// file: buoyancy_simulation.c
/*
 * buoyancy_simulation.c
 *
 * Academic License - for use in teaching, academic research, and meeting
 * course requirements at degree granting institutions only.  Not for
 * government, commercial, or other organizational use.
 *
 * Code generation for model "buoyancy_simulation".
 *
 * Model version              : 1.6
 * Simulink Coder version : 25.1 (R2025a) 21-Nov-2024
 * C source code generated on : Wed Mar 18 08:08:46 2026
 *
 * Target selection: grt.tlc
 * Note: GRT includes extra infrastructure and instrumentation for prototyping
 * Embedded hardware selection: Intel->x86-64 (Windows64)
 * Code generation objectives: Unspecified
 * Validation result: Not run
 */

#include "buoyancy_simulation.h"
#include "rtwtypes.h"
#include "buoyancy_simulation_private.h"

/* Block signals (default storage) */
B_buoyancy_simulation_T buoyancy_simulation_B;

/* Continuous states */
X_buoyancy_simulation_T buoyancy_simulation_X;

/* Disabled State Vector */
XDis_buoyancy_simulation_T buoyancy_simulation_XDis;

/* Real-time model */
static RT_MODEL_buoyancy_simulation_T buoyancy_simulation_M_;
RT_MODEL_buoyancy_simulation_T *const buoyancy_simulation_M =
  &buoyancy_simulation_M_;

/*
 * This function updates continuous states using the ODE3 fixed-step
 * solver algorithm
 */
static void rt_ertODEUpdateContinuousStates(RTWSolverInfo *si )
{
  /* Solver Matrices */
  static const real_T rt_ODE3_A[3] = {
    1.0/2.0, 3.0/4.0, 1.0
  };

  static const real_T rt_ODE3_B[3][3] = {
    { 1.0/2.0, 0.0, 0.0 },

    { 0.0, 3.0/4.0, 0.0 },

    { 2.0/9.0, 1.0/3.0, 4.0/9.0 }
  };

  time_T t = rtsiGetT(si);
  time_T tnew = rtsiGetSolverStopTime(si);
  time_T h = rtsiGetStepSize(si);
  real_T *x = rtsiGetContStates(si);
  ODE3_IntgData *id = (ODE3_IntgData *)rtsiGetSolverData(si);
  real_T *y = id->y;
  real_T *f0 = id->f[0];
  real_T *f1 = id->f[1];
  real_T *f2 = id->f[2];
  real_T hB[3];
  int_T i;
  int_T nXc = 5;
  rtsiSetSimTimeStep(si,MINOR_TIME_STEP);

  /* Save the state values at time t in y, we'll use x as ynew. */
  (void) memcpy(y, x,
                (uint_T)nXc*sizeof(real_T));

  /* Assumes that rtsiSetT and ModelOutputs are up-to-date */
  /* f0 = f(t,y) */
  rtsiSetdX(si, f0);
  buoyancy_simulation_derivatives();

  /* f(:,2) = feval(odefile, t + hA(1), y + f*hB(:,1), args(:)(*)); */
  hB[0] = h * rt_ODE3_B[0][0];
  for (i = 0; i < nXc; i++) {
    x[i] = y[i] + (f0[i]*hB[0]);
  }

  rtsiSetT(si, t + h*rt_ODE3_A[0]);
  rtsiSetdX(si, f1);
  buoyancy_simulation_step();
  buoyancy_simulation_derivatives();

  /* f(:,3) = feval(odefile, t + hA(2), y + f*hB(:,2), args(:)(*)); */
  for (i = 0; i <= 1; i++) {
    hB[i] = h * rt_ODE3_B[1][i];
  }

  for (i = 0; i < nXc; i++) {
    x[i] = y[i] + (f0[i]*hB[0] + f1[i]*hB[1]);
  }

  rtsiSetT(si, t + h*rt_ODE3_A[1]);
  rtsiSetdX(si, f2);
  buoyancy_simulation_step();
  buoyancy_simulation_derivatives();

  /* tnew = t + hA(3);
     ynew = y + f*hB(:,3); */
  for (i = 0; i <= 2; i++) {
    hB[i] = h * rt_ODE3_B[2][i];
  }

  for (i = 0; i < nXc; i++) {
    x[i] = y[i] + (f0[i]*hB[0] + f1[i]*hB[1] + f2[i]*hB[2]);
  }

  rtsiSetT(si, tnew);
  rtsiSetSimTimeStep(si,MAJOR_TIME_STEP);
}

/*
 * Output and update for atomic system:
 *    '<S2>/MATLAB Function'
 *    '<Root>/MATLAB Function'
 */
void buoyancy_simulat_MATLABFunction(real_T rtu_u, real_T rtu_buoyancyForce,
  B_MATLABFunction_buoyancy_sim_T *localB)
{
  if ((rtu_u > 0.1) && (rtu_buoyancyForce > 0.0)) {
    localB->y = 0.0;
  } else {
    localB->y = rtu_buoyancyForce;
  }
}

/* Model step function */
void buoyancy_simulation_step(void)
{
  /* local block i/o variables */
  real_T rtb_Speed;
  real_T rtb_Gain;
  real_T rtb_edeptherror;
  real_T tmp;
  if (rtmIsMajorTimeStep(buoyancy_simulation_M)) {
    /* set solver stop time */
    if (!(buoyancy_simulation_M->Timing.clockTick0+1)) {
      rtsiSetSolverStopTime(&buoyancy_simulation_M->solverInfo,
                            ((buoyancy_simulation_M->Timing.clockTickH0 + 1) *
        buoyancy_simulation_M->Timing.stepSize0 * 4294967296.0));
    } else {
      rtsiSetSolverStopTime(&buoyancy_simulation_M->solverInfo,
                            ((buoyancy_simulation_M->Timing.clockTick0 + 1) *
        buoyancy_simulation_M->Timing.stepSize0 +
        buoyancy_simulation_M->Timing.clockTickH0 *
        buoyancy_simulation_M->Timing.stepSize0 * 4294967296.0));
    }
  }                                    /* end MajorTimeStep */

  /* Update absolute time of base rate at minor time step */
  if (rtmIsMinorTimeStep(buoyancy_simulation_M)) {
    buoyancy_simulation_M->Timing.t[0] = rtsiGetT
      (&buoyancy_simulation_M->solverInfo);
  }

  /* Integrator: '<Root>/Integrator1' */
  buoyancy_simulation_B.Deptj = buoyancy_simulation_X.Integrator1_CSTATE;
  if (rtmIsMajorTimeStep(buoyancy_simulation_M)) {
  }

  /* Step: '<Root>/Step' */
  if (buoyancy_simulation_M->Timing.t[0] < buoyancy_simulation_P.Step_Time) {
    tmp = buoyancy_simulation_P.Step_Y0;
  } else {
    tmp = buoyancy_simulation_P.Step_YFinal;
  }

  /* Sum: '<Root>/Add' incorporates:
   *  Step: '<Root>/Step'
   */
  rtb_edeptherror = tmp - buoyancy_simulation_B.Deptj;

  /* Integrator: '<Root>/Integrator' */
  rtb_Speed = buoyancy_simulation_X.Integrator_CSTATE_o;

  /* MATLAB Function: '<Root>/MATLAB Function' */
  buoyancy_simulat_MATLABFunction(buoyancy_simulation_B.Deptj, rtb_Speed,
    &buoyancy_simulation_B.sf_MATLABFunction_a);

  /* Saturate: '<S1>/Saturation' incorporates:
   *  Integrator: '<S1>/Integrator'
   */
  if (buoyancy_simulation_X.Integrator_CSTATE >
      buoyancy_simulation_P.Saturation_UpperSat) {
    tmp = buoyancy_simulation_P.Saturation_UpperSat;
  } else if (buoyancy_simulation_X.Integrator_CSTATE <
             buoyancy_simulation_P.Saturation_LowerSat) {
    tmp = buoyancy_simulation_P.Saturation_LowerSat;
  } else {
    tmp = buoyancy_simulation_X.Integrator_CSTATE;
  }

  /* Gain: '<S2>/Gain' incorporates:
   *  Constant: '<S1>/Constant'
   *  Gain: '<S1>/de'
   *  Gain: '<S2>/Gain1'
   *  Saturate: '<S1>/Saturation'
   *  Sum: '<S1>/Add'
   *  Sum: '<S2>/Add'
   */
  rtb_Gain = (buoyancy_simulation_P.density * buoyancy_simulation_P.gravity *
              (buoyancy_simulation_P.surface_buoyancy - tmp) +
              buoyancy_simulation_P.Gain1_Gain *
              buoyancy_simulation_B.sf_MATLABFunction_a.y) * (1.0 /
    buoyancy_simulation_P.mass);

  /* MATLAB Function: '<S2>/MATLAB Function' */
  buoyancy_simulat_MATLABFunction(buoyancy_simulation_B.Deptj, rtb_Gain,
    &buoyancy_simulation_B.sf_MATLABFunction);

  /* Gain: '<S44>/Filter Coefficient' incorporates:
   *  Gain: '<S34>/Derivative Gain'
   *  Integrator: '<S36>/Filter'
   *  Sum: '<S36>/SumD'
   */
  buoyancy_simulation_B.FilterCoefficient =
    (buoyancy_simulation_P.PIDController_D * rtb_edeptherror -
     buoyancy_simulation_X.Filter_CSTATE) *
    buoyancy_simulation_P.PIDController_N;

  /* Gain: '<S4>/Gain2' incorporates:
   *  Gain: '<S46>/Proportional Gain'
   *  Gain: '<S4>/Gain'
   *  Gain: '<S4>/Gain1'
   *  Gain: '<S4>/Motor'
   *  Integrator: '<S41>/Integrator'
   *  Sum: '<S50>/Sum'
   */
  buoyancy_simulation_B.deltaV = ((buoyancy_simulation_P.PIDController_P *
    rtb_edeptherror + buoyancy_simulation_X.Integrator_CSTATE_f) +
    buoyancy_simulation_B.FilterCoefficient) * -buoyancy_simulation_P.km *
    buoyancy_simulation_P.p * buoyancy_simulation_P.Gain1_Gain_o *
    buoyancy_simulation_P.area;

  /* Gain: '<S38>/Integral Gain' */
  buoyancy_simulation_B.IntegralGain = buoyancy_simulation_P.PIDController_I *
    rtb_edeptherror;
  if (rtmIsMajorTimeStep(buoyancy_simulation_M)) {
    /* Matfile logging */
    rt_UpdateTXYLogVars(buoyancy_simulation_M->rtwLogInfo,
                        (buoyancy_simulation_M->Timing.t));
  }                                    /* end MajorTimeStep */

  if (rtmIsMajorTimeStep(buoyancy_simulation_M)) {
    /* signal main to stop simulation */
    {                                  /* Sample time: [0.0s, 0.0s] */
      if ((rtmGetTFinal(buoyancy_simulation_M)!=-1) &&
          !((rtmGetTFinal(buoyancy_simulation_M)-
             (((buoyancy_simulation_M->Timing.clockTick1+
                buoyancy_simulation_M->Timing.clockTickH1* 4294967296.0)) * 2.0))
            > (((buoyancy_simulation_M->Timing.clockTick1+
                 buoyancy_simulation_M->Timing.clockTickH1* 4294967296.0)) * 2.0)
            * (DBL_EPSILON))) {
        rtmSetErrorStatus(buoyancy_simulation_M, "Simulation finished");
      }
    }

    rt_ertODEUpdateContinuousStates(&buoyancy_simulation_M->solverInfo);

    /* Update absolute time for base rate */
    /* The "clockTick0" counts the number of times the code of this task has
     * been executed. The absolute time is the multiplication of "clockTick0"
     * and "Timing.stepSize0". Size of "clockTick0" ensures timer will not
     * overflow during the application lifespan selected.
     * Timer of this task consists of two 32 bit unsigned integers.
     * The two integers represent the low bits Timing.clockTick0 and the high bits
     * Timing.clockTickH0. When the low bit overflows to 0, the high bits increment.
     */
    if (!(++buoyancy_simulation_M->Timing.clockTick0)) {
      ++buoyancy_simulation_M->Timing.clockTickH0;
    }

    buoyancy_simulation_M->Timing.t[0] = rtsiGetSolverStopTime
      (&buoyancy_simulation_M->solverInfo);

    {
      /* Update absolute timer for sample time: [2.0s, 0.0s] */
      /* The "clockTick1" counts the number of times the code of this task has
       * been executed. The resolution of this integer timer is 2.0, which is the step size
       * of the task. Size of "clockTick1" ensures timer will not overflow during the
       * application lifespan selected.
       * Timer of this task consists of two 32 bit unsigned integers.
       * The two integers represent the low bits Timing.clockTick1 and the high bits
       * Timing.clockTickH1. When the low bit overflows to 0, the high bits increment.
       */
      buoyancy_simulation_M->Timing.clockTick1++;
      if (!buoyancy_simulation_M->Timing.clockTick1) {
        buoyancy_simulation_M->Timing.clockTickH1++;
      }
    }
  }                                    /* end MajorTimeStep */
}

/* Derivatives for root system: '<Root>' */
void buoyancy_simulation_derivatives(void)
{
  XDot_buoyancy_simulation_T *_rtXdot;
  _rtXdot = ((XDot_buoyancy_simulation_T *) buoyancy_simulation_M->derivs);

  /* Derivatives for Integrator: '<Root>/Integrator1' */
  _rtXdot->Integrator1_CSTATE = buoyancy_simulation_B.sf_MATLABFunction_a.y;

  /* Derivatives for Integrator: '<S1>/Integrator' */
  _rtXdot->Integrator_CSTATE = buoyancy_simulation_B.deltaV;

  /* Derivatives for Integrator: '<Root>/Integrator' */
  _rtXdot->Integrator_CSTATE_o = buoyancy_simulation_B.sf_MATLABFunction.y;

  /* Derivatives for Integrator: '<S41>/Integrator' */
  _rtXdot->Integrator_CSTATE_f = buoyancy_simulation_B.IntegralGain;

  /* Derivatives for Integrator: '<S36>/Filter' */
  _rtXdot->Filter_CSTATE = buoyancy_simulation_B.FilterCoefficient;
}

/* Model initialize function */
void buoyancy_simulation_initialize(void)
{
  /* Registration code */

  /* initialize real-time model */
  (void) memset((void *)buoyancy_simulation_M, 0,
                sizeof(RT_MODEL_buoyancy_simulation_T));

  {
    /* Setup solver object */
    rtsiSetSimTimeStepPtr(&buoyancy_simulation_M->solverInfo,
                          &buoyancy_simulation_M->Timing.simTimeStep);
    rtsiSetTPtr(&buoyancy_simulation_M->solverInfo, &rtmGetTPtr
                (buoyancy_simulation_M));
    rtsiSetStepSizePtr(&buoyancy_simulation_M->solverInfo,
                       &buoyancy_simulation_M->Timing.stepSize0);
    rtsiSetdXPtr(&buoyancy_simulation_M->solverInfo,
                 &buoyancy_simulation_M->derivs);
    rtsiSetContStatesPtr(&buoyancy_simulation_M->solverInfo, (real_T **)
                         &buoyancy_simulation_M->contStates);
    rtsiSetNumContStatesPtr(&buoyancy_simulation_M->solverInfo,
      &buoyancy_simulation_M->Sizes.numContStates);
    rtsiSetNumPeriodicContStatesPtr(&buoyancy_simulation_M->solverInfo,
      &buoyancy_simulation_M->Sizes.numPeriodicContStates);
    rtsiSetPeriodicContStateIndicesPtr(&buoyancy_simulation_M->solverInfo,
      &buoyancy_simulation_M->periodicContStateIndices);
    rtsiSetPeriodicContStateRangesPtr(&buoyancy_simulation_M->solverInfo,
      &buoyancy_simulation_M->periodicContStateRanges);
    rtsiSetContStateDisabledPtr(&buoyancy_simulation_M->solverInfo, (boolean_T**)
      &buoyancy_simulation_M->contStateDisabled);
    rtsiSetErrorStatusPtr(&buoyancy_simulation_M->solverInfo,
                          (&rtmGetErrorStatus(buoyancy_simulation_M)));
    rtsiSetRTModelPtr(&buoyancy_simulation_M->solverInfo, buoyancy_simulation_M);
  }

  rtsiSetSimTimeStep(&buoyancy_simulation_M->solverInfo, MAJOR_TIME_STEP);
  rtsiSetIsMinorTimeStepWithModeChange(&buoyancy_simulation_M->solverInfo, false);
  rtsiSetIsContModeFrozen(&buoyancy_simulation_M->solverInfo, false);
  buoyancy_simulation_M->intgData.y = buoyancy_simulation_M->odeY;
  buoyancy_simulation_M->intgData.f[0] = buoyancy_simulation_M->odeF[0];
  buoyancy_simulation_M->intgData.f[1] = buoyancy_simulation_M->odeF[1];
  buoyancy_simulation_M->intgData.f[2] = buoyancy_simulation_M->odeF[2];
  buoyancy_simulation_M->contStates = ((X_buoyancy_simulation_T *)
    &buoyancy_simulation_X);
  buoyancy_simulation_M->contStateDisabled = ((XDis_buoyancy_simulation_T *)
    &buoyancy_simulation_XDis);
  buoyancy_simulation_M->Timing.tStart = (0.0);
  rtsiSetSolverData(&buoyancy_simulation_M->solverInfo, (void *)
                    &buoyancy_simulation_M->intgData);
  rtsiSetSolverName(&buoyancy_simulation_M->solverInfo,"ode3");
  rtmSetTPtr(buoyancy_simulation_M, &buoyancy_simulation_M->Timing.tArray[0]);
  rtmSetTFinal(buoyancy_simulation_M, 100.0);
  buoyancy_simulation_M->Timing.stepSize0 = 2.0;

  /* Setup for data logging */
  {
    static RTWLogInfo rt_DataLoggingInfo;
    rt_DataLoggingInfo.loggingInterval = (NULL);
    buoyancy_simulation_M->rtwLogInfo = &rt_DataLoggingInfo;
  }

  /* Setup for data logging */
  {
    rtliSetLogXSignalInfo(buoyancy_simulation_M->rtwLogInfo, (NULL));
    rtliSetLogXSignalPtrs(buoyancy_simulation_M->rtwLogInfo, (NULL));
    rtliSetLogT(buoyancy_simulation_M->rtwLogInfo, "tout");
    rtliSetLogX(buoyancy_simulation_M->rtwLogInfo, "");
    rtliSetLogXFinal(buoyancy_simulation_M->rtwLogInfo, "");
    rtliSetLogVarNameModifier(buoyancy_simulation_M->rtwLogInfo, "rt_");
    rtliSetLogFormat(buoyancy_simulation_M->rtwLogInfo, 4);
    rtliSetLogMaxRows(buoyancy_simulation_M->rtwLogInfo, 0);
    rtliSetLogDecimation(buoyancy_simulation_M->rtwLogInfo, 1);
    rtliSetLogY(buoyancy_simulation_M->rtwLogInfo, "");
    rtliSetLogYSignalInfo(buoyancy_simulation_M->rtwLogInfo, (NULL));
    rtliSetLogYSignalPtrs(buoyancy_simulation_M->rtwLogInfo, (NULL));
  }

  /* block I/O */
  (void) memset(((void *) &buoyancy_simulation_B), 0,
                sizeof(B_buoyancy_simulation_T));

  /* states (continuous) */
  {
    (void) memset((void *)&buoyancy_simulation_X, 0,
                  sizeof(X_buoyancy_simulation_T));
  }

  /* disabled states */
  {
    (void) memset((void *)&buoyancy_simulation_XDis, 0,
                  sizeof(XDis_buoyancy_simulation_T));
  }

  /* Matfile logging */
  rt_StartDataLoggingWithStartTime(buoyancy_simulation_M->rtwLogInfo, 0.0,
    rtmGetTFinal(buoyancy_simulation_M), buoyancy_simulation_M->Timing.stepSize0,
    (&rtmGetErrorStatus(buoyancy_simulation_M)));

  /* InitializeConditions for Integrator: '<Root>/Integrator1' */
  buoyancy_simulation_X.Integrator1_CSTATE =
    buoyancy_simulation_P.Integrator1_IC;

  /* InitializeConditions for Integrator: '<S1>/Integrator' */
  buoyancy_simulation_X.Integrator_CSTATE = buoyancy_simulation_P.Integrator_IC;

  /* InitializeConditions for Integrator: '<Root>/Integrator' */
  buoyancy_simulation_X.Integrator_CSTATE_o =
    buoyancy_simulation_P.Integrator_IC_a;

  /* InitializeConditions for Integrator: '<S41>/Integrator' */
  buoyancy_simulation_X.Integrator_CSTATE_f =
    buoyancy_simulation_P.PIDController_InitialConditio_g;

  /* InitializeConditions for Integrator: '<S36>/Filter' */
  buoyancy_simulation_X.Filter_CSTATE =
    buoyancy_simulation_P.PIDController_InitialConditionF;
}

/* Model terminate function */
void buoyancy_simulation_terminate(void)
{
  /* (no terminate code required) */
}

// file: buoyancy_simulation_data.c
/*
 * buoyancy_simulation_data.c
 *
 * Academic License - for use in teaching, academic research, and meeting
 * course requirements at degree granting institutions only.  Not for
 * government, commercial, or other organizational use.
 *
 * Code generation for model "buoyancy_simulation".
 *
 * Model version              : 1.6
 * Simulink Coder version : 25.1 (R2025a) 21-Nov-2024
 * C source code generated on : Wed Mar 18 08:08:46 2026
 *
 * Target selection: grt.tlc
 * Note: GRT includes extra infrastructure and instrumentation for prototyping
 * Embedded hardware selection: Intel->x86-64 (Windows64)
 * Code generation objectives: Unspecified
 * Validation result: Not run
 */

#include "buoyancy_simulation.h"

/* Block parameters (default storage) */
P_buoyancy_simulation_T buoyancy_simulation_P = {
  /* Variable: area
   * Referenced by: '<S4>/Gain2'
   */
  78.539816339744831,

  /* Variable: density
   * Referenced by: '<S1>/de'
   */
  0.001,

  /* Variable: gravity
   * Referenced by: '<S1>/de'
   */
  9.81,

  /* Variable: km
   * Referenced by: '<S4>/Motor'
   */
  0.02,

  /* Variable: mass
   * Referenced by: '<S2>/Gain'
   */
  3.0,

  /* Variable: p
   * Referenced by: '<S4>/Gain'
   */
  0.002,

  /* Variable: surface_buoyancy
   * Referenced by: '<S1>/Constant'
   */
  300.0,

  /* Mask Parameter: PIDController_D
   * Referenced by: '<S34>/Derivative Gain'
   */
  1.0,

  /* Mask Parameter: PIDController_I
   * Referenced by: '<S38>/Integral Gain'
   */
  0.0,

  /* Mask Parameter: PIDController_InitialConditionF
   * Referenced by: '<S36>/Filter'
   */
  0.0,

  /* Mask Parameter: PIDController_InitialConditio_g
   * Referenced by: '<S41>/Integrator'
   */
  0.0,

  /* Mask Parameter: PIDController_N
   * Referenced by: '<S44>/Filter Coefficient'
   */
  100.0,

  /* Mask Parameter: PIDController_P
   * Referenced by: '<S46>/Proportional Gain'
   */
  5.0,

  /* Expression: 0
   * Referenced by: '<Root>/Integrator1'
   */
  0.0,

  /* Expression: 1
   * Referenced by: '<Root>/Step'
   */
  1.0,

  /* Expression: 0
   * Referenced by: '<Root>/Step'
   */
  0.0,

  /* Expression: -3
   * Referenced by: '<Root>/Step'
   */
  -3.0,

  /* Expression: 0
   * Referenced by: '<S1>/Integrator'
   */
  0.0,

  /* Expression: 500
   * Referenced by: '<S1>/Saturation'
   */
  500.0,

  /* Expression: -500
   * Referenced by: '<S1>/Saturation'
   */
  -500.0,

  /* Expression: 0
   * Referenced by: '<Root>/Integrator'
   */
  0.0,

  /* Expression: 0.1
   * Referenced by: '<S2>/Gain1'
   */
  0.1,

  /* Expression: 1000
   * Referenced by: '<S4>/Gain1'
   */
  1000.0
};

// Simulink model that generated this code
simulink model "buoyancy_simulation"  (R2025a)
settings: Solver=VariableStepAuto  StartTime=0.0  StopTime=100  RelTol=1e-3
InitFcn:
  | parameters
values from neighbouring files (symbols this model uses):
  area = pi*(d/2)^2    (= 0.00785398163397)    [parameters.m]    (also in simulation_matlab.m)
  density = 1000    [parameters.m]
  gravity = 9.81    [parameters.m]
  km = 50    [parameters.m]
  mass = 3    [parameters.m]
  p = 0.002    [parameters.m]    (also in simulation_matlab.m)
  surface_buoyancy = 2.94    [parameters.m]
libraries: slpidlib x1

== system buoyancy_simulation ==
  Add : Sum  Inputs=+-
  Buoyant force : Subsystem
  Heave Plant : Subsystem
  Integrator : Integrator
  Integrator1 : Integrator
  MATLAB Function : MATLAB Function  TreatAsAtomicUnit=on
  Motor and lead screw : Subsystem
  PID Controller : slpidlib/PID Controller  Controller=PID  Form=Parallel  TimeDomain=Continuous-time  UseExternalTs=off  SampleTime=-1  IntegratorMethod=Forward Euler  FilterMethod=Forward Euler  ControllerParametersSource=internal  P=5  I=0  UseKiTs=off  D=1  UseExternalDerivativeSource=off  N=100  UseFilter=on  TunerSelectOption=Transfer Function Based (PID Tuner App)  InitialConditionSource=internal  InitialConditionForIntegrator=0  InitialConditionForFilter=0  DifferentiatorICPrevScaledInput=0  ExternalReset=none  TrackingMode=off  Kt=1  LimitOutput=off  SatLimitsSource=internal  UpperSaturationLimit=inf  LowerSaturationLimit=-inf  LinearizeAsGain=on  AntiWindupMode=none  Kb=1  LimitIntegrator=off  UpperIntegratorSaturationLimit=inf  LowerIntegratorSaturationLimit=-inf  POutMin=[]  POutMax=[]  IOutMin=[]  IOutMax=[]  DOutMin=[]  DOutMax=[]  NOutMin=[]  NOutMax=[]  SumOutMin=[]  SumOutMax=[]  SaturationOutMin=[]  SaturationOutMax=[]  PParamMin=[]  PParamMax=[]  IParamMin=[]  IParamMax=[]  DParamMin=[]  DParamMax=[]  NParamMin=[]  NParamMax=[]  KbParamMin=[]  KbParamMax=[]  KtParamMin=[]  KtParamMax=[]  KbOutMin=[]  KbOutMax=[]  KtOutMin=[]  KtOutMax=[]  IntegratorOutMin=[]  IntegratorOutMax=[]  FilterOutMin=[]  FilterOutMax=[]  SumI1OutMin=[]  SumI1OutMax=[]  SumI2OutMin=[]  SumI2OutMax=[]  SumI3OutMin=[]  SumI3OutMax=[]  SumI4OutMin=[]  SumI4OutMax=[]  SumDOutMin=[]  SumDOutMax=[]  DifferentiatorOutMin=[]  DifferentiatorOutMax=[]  FilterDiffOutCoefMin=[]  FilterDiffOutCoefMax=[]  ReciprocalOutMin=[]  ReciprocalOutMax=[]  SumDenOutMin=[]  SumDenOutMax=[]  SumNumOutMin=[]  SumNumOutMax=[]  DivideOutMin=[]  DivideOutMax=[]  UdiffTsProdOutMin=[]  UdiffTsProdOutMax=[]  NTsProdOutMin=[]  NTsProdOutMax=[]  UintegralTsProdOutMin=[]  UintegralTsProdOutMax=[]  UngainTsProdOutMin=[]  UngainTsProdOutMax=[]  ClampingZeroOutDataTypeStr=Inherit: Inherit via back propagation  ClampingZeroOutMin=[]  ClampingZeroOutMax=[]  FilterDenConstantOutDataTypeStr=Inherit: Inherit via back propagation  FilterDenConstantOutMin=[]  FilterDenConstantOutMax=[]  PCopyOutDataTypeStr=Inherit: Inherit via back propagation  PCopyOutMin=[]  PCopyOutMax=[]  NCopyOutDataTypeStr=Inherit: Inherit via back propagation  NCopyOutMin=[]  NCopyOutMax=[]  IntegratorContinuousStateAttributes=''  IntegratorStateMustResolveToSignalObject=off  IntegratorRTWStateStorageClass=Auto  FilterContinuousStateAttributes=''  FilterStateMustResolveToSignalObject=off  FilterRTWStateStorageClass=Auto  ParallelPVariant=InternalParameters  IdealPVariant=Disabled  IVariant=InternalParameters  DVariant=InternalParameters  IntegratorVariant=Continuous  SatVariant=Disabled  AWVariant=Passthrough  PCopyVariant=Disabled  TRVariant=Disabled  FdbkBlocksVariant=Forward  IdealPFdbkVariant=Disabled  SatFdbkVariant=Disabled  DerivativeFilterVariant=ContFilter  NVariant=InternalParameters  NCopyVariant=Disabled  FilterICVariant=InternalICsFilter  IntegratorICVariant=InternalICs  ExternalResetVariant=Disabled  TRSumVariant=Passthrough  SumFdbkVariant=Disabled  SumVariant=Sum_PID  TsampFilterVariant=InternalTs  TsampNgainVariant=Passthrough  TsampIntegralVariant=Disabled_SignalSpec  ExternalSaturationOutDataTypeStr=Inherit: Same as second input  DerivativeSourceVariant=ErrorSignal  PreIntVariant=InternalPreInt
  Scope : Scope
  Step : Step  After=-3  SampleTime=0
  wires:
  Step/1 -> Add/1  "Ref_depth"
  Heave Plant/1(y) -> Integrator/1  "Speed"
  Add/1 -> PID Controller/1  "e (depth error)"
  PID Controller/1 -> Motor and lead screw/1(In1)  "u, control signal"
  Motor and lead screw/1(Out1) -> Buoyant force/1(In1)  "deltaV"
  Buoyant force/1(Out1) -> Heave Plant/1(In1)  "Buoyant force"
  Integrator/1 -> MATLAB Function/2(buoyancyForce)  "Speed`+"
  Integrator1/1 -> Scope/1, MATLAB Function/1(u), Heave Plant/3(buoyancyForce), Add/2  "Deptj"
  MATLAB Function/1(y) -> Integrator1/1, Heave Plant/2(In2)

== system buoyancy_simulation/Buoyant force ==
  In1 : Inport
  Add : Sum  Inputs=-+
  Constant : Constant  Value=surface_buoyancy
  Integrator : Integrator
  Saturation : Saturate  UpperLimit=500  LowerLimit=-500
  de : Gain  Gain=density*gravity
  Out1 : Outport
  wires:
  In1/1 -> Integrator/1  "deltaV"
  Integrator/1 -> Saturation/1  "new_V"
  Add/1 -> de/1
  Constant/1 -> Add/2
  Saturation/1 -> Add/1  "saturated V"
  de/1 -> Out1/1

== system buoyancy_simulation/Heave Plant ==
  In1 : Inport
  In2 : Inport  Port=2
  buoyancyForce : Inport  Port=3
  Add : Sum
  Gain : Gain  Gain=1/mass
  Gain1 : Gain  Gain=0.1
  MATLAB Function : MATLAB Function  TreatAsAtomicUnit=on
  y : Outport
  wires:
  Add/1 -> Gain/1
  Gain1/1 -> Add/2
  In2/1 -> Gain1/1
  MATLAB Function/1(y) -> y/1
  buoyancyForce/1 -> MATLAB Function/1(u)
  Gain/1 -> MATLAB Function/2(buoyancyForce)
  In1/1 -> Add/1

== system buoyancy_simulation/Motor and lead screw ==
  In1 : Inport
  Gain : Gain  Gain=p
  Gain1 : Gain  Gain=1000
  Gain2 : Gain  Gain=area
  Motor : Gain  Gain=-km
  Out1 : Outport
  wires:
  In1/1 -> Motor/1  "PWM"
  Motor/1 -> Gain/1  "Rotation"
  Gain/1 -> Gain1/1  "Linear displacement"
  Gain2/1 -> Out1/1  "deltaV"
  Gain1/1 -> Gain2/1  "Linear displacement mm"

== matlab function buoyancy_simulation/Heave Plant/MATLAB Function ==
function y = fcn(u, buoyancyForce)
    if u > 0.1 && buoyancyForce > 0
        y = 0;
    else
        y = buoyancyForce;
    end
end

== matlab function buoyancy_simulation/MATLAB Function ==
function y = fcn(u, buoyancyForce)
    if u > 0.1 && buoyancyForce > 0
        y = 0;
    else
        y = buoyancyForce;
    end
end
